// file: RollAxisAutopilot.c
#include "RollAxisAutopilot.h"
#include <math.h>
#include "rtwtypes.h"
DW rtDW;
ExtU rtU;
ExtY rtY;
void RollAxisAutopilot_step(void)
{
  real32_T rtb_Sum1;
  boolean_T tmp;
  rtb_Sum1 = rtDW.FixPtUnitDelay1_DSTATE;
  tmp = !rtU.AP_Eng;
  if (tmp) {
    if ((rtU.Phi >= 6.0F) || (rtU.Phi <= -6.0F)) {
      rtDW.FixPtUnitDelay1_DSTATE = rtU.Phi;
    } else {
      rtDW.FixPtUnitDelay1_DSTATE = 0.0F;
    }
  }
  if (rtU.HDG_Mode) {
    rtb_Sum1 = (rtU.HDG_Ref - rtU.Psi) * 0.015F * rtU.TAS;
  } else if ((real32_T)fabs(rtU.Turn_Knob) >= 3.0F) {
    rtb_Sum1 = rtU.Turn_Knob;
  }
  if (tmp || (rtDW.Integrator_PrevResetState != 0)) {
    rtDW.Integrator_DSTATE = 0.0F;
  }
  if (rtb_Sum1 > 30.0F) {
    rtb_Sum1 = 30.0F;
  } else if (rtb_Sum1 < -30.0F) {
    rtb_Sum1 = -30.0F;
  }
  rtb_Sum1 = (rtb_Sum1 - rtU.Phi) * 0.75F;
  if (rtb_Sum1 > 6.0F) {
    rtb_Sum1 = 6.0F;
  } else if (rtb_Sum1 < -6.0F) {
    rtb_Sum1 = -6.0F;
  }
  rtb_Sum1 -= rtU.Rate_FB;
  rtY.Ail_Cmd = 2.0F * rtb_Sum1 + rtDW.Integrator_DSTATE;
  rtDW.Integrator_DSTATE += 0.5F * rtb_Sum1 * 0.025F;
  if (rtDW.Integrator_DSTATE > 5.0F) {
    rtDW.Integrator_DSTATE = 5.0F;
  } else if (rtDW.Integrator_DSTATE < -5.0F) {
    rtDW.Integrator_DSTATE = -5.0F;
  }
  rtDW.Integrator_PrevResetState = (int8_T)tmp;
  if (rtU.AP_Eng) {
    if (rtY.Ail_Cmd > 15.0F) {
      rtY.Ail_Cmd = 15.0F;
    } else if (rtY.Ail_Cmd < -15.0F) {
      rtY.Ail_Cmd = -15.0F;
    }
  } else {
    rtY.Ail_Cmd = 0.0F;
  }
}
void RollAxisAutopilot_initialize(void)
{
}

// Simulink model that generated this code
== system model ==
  Phi : Inport
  Psi : Inport
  Rate_FB : Inport
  TAS : Inport
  AP_Eng : Inport
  HDG_Mode : Inport
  HDG_Ref : Inport
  Turn_Knob : Inport
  Ail_Cmd : Outport  <- 1: Switch#1
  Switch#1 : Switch  Criteria=u2 ~= 0  <- 1: Subsystem#1, 2: AP_Eng, 3: Constant#1
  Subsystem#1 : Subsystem  <- 1: Switch#2, 2: Phi, 3: Rate_FB, 4: AP_Eng
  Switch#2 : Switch  Criteria=u2 ~= 0  <- 1: Subsystem#2, 2: HDG_Mode, 3: Subsystem#3
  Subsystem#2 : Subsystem  <- 1: HDG_Ref, 2: Psi, 3: TAS
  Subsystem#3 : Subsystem  <- 1: Phi, 2: AP_Eng, 3: Turn_Knob
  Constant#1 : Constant  Value=0
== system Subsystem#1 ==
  Inport#1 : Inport
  Inport#2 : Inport
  Inport#3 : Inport
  Inport#4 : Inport
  Outport#1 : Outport  <- 1: Saturate#1
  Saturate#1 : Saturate  UpperLimit=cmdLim  LowerLimit=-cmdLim  <- 1: Sum#1
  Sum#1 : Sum  Inputs=++  <- 1: Integrator, 2: Gain#1
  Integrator : DiscreteIntegrator  ExternalReset=level  LimitOutput=on  UpperSaturationLimit=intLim  LowerSaturationLimit=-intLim  <- 1: Gain#2, 2: Logic#1
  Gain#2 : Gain  Gain=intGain  <- 1: Sum1
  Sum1 : Sum  Inputs=+-  <- 1: Saturate#2, 2: Inport#3
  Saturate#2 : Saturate  UpperLimit=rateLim  LowerLimit=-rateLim  <- 1: Gain#3
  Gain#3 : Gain  Gain=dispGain  <- 1: Sum#2
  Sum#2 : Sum  Inputs=+-  <- 1: Saturate#3, 2: Inport#2
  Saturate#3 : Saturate  UpperLimit=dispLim  LowerLimit=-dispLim  <- 1: Inport#1
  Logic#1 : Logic  Operator=NOT  <- 1: Inport#4
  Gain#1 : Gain  Gain=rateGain  <- 1: Sum1
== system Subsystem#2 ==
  Inport#5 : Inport
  Inport#6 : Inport
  Inport#7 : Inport
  Outport#2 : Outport  <- 1: Product#1
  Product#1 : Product  <- 1: Gain#4, 2: Inport#7
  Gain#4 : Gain  Gain=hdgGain  <- 1: Sum#3
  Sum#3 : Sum  Inputs=+-  <- 1: Inport#5, 2: Inport#6
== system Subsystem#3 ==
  Inport#8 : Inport
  Inport#9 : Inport
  Inport#10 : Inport
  Outport#3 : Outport  <- 1: Switch#3
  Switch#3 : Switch  Criteria=u2 ~= 0  <- 1: UnitDelayEnabled#1, 2: RelationalOperator#1, 3: Inport#10
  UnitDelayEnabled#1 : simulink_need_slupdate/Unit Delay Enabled  <- 1: Switch#4, 2: Logic#2
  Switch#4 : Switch  Criteria=u2 ~= 0  <- 1: Inport#8, 2: Logic#3, 3: Constant#2
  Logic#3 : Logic  Operator=OR  <- 1: RelationalOperator#2, 2: RelationalOperator#3
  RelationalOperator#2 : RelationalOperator  <- 1: Inport#8, 2: Constant#3
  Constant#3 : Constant  Value=6
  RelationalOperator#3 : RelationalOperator  Operator=<=  <- 1: Inport#8, 2: Constant#4
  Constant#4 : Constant  Value=-6
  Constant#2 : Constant  Value=0
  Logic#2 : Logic  Operator=NOT  <- 1: Inport#9
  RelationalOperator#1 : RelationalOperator  Operator=<  <- 1: Abs#1, 2: Constant#5
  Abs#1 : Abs  <- 1: Inport#10
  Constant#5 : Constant  Value=3
